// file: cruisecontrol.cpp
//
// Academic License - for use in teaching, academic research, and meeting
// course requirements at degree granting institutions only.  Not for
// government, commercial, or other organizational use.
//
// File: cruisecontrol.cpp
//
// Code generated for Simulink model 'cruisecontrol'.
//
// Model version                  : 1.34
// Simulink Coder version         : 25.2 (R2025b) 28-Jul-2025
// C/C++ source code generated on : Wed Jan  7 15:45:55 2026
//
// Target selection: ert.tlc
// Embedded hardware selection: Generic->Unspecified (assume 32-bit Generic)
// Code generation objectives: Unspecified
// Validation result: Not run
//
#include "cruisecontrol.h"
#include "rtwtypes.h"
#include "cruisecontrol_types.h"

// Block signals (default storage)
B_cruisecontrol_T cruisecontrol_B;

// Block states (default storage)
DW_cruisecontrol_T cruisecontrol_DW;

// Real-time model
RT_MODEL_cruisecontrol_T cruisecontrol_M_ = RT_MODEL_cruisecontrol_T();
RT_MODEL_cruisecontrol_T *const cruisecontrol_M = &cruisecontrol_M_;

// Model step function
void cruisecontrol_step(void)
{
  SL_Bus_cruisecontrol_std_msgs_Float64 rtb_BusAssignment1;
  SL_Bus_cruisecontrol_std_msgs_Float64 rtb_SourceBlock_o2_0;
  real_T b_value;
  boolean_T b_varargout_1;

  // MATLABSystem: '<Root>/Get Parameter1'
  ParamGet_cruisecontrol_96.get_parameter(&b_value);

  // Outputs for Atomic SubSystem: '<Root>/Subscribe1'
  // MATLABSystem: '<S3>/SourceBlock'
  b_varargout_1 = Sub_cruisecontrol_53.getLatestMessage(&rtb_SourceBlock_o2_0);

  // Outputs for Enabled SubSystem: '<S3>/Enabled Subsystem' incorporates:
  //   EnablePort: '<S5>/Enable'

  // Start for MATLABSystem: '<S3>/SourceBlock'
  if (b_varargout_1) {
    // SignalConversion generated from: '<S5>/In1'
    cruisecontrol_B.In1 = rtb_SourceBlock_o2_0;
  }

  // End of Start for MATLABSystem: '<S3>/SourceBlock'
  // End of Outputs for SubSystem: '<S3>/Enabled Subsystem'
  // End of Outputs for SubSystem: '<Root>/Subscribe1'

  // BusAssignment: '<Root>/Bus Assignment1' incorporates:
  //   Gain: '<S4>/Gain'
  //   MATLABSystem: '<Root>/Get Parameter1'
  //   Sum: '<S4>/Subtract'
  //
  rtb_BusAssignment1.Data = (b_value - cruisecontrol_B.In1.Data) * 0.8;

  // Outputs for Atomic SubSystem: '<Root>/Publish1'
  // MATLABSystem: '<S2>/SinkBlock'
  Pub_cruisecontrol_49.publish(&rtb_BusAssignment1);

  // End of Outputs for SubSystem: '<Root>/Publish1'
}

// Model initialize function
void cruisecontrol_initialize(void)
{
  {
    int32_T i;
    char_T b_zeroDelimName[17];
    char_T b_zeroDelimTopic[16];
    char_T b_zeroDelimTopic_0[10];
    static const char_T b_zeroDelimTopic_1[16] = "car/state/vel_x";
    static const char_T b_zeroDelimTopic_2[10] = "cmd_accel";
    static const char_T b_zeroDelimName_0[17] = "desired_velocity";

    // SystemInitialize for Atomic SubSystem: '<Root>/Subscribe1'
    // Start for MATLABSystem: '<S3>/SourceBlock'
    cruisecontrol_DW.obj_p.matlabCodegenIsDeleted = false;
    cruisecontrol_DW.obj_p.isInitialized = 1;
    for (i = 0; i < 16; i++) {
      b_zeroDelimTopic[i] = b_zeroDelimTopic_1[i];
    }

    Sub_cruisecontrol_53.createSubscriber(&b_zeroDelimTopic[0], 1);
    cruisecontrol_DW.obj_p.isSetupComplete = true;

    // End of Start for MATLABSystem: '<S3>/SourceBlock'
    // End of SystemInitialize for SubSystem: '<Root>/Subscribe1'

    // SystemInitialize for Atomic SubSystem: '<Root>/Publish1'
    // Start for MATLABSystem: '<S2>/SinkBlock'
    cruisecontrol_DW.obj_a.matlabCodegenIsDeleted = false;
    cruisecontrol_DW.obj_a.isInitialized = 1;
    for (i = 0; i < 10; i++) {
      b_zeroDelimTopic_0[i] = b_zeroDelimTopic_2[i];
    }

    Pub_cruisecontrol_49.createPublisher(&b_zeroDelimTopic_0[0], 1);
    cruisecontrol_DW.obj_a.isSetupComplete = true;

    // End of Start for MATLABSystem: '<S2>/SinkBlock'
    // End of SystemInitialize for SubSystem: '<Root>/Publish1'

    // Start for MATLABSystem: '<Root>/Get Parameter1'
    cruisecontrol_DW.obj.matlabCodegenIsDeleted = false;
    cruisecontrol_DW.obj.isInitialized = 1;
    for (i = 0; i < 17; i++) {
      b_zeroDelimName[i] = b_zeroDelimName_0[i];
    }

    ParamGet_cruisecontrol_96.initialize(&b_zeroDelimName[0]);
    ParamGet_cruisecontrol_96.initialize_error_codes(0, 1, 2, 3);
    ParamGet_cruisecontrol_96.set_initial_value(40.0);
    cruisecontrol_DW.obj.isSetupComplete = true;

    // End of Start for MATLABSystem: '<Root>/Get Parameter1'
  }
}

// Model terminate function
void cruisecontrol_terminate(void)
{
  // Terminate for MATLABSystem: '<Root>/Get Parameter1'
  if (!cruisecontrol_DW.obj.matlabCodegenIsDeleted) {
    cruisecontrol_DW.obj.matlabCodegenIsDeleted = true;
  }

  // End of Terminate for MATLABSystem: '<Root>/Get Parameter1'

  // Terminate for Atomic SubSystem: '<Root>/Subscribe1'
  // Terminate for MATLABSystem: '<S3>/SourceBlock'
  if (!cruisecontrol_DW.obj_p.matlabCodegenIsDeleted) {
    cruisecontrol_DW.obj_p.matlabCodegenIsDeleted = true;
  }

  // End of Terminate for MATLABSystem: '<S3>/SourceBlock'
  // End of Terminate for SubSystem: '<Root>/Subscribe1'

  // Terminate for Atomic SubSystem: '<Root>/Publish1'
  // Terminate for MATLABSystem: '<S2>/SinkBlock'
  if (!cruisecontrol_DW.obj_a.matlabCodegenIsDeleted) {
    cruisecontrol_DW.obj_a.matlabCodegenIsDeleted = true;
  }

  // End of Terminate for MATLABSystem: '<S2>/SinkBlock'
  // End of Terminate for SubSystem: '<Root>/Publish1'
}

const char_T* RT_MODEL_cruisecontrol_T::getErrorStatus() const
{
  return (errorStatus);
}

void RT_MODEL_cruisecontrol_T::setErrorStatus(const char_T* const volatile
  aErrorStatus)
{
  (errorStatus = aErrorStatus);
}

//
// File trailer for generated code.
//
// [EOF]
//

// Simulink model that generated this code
simulink model "cruisecontrol"  (R2025b)
settings: Solver=FixedStepAuto  StartTime=0.0  StopTime=inf  FixedStep=0.05  RelTol=1e-3
libraries: robotlib x4

== system cruisecontrol ==
  Blank Message1 : robotlib/Blank Message  messageClass=Message  entityType=std_msgs/Float64  messageType=std_msgs/Float64  SampleTime=inf  legacyBusStruct=off
  Bus Assignment1 : BusAssignment  AssignedSignals=Data
  Bus Selector1 : BusSelector  OutputSignals=Data
  Get Parameter1 : robotlib/Get Parameter  ParameterSource=Specify your own  ParameterName=desired_velocity  ParameterType=double  ParameterMaxArrayLength=16  ParameterInitialValue=40  SampleTime=-1  ShowErrorCodeOutput=on  ModelName=cruisecontrol  BlockId=ParamGet_cruisecontrol_96
  Publish1 : robotlib/Publish  topicSource=Specify your own  topic=cmd_accel  messageType=std_msgs/Float64  legacyBusStruct=off  messageQueueLength=1
  Subscribe1 : robotlib/Subscribe  topicSource=Specify your own  topic=car/state/vel_x  messageType=std_msgs/Float64  SampleTime=-1  legacyBusStruct=off  messageQueueLength=1
  Subsystem Reference : Subsystem  ReferencedSubsystem=acc_nom
  Terminator1 : Terminator
  wires:
  Bus Assignment1/1 -> Publish1/1
  Subscribe1/2 -> Bus Selector1/1
  Bus Selector1/1 -> Subsystem Reference/1  "<Data>"
  Subscribe1/1 -> Terminator1/1
  Subsystem Reference/1 -> Bus Assignment1/2
  Blank Message1/1 -> Bus Assignment1/1
  Get Parameter1/1 -> Subsystem Reference/2
